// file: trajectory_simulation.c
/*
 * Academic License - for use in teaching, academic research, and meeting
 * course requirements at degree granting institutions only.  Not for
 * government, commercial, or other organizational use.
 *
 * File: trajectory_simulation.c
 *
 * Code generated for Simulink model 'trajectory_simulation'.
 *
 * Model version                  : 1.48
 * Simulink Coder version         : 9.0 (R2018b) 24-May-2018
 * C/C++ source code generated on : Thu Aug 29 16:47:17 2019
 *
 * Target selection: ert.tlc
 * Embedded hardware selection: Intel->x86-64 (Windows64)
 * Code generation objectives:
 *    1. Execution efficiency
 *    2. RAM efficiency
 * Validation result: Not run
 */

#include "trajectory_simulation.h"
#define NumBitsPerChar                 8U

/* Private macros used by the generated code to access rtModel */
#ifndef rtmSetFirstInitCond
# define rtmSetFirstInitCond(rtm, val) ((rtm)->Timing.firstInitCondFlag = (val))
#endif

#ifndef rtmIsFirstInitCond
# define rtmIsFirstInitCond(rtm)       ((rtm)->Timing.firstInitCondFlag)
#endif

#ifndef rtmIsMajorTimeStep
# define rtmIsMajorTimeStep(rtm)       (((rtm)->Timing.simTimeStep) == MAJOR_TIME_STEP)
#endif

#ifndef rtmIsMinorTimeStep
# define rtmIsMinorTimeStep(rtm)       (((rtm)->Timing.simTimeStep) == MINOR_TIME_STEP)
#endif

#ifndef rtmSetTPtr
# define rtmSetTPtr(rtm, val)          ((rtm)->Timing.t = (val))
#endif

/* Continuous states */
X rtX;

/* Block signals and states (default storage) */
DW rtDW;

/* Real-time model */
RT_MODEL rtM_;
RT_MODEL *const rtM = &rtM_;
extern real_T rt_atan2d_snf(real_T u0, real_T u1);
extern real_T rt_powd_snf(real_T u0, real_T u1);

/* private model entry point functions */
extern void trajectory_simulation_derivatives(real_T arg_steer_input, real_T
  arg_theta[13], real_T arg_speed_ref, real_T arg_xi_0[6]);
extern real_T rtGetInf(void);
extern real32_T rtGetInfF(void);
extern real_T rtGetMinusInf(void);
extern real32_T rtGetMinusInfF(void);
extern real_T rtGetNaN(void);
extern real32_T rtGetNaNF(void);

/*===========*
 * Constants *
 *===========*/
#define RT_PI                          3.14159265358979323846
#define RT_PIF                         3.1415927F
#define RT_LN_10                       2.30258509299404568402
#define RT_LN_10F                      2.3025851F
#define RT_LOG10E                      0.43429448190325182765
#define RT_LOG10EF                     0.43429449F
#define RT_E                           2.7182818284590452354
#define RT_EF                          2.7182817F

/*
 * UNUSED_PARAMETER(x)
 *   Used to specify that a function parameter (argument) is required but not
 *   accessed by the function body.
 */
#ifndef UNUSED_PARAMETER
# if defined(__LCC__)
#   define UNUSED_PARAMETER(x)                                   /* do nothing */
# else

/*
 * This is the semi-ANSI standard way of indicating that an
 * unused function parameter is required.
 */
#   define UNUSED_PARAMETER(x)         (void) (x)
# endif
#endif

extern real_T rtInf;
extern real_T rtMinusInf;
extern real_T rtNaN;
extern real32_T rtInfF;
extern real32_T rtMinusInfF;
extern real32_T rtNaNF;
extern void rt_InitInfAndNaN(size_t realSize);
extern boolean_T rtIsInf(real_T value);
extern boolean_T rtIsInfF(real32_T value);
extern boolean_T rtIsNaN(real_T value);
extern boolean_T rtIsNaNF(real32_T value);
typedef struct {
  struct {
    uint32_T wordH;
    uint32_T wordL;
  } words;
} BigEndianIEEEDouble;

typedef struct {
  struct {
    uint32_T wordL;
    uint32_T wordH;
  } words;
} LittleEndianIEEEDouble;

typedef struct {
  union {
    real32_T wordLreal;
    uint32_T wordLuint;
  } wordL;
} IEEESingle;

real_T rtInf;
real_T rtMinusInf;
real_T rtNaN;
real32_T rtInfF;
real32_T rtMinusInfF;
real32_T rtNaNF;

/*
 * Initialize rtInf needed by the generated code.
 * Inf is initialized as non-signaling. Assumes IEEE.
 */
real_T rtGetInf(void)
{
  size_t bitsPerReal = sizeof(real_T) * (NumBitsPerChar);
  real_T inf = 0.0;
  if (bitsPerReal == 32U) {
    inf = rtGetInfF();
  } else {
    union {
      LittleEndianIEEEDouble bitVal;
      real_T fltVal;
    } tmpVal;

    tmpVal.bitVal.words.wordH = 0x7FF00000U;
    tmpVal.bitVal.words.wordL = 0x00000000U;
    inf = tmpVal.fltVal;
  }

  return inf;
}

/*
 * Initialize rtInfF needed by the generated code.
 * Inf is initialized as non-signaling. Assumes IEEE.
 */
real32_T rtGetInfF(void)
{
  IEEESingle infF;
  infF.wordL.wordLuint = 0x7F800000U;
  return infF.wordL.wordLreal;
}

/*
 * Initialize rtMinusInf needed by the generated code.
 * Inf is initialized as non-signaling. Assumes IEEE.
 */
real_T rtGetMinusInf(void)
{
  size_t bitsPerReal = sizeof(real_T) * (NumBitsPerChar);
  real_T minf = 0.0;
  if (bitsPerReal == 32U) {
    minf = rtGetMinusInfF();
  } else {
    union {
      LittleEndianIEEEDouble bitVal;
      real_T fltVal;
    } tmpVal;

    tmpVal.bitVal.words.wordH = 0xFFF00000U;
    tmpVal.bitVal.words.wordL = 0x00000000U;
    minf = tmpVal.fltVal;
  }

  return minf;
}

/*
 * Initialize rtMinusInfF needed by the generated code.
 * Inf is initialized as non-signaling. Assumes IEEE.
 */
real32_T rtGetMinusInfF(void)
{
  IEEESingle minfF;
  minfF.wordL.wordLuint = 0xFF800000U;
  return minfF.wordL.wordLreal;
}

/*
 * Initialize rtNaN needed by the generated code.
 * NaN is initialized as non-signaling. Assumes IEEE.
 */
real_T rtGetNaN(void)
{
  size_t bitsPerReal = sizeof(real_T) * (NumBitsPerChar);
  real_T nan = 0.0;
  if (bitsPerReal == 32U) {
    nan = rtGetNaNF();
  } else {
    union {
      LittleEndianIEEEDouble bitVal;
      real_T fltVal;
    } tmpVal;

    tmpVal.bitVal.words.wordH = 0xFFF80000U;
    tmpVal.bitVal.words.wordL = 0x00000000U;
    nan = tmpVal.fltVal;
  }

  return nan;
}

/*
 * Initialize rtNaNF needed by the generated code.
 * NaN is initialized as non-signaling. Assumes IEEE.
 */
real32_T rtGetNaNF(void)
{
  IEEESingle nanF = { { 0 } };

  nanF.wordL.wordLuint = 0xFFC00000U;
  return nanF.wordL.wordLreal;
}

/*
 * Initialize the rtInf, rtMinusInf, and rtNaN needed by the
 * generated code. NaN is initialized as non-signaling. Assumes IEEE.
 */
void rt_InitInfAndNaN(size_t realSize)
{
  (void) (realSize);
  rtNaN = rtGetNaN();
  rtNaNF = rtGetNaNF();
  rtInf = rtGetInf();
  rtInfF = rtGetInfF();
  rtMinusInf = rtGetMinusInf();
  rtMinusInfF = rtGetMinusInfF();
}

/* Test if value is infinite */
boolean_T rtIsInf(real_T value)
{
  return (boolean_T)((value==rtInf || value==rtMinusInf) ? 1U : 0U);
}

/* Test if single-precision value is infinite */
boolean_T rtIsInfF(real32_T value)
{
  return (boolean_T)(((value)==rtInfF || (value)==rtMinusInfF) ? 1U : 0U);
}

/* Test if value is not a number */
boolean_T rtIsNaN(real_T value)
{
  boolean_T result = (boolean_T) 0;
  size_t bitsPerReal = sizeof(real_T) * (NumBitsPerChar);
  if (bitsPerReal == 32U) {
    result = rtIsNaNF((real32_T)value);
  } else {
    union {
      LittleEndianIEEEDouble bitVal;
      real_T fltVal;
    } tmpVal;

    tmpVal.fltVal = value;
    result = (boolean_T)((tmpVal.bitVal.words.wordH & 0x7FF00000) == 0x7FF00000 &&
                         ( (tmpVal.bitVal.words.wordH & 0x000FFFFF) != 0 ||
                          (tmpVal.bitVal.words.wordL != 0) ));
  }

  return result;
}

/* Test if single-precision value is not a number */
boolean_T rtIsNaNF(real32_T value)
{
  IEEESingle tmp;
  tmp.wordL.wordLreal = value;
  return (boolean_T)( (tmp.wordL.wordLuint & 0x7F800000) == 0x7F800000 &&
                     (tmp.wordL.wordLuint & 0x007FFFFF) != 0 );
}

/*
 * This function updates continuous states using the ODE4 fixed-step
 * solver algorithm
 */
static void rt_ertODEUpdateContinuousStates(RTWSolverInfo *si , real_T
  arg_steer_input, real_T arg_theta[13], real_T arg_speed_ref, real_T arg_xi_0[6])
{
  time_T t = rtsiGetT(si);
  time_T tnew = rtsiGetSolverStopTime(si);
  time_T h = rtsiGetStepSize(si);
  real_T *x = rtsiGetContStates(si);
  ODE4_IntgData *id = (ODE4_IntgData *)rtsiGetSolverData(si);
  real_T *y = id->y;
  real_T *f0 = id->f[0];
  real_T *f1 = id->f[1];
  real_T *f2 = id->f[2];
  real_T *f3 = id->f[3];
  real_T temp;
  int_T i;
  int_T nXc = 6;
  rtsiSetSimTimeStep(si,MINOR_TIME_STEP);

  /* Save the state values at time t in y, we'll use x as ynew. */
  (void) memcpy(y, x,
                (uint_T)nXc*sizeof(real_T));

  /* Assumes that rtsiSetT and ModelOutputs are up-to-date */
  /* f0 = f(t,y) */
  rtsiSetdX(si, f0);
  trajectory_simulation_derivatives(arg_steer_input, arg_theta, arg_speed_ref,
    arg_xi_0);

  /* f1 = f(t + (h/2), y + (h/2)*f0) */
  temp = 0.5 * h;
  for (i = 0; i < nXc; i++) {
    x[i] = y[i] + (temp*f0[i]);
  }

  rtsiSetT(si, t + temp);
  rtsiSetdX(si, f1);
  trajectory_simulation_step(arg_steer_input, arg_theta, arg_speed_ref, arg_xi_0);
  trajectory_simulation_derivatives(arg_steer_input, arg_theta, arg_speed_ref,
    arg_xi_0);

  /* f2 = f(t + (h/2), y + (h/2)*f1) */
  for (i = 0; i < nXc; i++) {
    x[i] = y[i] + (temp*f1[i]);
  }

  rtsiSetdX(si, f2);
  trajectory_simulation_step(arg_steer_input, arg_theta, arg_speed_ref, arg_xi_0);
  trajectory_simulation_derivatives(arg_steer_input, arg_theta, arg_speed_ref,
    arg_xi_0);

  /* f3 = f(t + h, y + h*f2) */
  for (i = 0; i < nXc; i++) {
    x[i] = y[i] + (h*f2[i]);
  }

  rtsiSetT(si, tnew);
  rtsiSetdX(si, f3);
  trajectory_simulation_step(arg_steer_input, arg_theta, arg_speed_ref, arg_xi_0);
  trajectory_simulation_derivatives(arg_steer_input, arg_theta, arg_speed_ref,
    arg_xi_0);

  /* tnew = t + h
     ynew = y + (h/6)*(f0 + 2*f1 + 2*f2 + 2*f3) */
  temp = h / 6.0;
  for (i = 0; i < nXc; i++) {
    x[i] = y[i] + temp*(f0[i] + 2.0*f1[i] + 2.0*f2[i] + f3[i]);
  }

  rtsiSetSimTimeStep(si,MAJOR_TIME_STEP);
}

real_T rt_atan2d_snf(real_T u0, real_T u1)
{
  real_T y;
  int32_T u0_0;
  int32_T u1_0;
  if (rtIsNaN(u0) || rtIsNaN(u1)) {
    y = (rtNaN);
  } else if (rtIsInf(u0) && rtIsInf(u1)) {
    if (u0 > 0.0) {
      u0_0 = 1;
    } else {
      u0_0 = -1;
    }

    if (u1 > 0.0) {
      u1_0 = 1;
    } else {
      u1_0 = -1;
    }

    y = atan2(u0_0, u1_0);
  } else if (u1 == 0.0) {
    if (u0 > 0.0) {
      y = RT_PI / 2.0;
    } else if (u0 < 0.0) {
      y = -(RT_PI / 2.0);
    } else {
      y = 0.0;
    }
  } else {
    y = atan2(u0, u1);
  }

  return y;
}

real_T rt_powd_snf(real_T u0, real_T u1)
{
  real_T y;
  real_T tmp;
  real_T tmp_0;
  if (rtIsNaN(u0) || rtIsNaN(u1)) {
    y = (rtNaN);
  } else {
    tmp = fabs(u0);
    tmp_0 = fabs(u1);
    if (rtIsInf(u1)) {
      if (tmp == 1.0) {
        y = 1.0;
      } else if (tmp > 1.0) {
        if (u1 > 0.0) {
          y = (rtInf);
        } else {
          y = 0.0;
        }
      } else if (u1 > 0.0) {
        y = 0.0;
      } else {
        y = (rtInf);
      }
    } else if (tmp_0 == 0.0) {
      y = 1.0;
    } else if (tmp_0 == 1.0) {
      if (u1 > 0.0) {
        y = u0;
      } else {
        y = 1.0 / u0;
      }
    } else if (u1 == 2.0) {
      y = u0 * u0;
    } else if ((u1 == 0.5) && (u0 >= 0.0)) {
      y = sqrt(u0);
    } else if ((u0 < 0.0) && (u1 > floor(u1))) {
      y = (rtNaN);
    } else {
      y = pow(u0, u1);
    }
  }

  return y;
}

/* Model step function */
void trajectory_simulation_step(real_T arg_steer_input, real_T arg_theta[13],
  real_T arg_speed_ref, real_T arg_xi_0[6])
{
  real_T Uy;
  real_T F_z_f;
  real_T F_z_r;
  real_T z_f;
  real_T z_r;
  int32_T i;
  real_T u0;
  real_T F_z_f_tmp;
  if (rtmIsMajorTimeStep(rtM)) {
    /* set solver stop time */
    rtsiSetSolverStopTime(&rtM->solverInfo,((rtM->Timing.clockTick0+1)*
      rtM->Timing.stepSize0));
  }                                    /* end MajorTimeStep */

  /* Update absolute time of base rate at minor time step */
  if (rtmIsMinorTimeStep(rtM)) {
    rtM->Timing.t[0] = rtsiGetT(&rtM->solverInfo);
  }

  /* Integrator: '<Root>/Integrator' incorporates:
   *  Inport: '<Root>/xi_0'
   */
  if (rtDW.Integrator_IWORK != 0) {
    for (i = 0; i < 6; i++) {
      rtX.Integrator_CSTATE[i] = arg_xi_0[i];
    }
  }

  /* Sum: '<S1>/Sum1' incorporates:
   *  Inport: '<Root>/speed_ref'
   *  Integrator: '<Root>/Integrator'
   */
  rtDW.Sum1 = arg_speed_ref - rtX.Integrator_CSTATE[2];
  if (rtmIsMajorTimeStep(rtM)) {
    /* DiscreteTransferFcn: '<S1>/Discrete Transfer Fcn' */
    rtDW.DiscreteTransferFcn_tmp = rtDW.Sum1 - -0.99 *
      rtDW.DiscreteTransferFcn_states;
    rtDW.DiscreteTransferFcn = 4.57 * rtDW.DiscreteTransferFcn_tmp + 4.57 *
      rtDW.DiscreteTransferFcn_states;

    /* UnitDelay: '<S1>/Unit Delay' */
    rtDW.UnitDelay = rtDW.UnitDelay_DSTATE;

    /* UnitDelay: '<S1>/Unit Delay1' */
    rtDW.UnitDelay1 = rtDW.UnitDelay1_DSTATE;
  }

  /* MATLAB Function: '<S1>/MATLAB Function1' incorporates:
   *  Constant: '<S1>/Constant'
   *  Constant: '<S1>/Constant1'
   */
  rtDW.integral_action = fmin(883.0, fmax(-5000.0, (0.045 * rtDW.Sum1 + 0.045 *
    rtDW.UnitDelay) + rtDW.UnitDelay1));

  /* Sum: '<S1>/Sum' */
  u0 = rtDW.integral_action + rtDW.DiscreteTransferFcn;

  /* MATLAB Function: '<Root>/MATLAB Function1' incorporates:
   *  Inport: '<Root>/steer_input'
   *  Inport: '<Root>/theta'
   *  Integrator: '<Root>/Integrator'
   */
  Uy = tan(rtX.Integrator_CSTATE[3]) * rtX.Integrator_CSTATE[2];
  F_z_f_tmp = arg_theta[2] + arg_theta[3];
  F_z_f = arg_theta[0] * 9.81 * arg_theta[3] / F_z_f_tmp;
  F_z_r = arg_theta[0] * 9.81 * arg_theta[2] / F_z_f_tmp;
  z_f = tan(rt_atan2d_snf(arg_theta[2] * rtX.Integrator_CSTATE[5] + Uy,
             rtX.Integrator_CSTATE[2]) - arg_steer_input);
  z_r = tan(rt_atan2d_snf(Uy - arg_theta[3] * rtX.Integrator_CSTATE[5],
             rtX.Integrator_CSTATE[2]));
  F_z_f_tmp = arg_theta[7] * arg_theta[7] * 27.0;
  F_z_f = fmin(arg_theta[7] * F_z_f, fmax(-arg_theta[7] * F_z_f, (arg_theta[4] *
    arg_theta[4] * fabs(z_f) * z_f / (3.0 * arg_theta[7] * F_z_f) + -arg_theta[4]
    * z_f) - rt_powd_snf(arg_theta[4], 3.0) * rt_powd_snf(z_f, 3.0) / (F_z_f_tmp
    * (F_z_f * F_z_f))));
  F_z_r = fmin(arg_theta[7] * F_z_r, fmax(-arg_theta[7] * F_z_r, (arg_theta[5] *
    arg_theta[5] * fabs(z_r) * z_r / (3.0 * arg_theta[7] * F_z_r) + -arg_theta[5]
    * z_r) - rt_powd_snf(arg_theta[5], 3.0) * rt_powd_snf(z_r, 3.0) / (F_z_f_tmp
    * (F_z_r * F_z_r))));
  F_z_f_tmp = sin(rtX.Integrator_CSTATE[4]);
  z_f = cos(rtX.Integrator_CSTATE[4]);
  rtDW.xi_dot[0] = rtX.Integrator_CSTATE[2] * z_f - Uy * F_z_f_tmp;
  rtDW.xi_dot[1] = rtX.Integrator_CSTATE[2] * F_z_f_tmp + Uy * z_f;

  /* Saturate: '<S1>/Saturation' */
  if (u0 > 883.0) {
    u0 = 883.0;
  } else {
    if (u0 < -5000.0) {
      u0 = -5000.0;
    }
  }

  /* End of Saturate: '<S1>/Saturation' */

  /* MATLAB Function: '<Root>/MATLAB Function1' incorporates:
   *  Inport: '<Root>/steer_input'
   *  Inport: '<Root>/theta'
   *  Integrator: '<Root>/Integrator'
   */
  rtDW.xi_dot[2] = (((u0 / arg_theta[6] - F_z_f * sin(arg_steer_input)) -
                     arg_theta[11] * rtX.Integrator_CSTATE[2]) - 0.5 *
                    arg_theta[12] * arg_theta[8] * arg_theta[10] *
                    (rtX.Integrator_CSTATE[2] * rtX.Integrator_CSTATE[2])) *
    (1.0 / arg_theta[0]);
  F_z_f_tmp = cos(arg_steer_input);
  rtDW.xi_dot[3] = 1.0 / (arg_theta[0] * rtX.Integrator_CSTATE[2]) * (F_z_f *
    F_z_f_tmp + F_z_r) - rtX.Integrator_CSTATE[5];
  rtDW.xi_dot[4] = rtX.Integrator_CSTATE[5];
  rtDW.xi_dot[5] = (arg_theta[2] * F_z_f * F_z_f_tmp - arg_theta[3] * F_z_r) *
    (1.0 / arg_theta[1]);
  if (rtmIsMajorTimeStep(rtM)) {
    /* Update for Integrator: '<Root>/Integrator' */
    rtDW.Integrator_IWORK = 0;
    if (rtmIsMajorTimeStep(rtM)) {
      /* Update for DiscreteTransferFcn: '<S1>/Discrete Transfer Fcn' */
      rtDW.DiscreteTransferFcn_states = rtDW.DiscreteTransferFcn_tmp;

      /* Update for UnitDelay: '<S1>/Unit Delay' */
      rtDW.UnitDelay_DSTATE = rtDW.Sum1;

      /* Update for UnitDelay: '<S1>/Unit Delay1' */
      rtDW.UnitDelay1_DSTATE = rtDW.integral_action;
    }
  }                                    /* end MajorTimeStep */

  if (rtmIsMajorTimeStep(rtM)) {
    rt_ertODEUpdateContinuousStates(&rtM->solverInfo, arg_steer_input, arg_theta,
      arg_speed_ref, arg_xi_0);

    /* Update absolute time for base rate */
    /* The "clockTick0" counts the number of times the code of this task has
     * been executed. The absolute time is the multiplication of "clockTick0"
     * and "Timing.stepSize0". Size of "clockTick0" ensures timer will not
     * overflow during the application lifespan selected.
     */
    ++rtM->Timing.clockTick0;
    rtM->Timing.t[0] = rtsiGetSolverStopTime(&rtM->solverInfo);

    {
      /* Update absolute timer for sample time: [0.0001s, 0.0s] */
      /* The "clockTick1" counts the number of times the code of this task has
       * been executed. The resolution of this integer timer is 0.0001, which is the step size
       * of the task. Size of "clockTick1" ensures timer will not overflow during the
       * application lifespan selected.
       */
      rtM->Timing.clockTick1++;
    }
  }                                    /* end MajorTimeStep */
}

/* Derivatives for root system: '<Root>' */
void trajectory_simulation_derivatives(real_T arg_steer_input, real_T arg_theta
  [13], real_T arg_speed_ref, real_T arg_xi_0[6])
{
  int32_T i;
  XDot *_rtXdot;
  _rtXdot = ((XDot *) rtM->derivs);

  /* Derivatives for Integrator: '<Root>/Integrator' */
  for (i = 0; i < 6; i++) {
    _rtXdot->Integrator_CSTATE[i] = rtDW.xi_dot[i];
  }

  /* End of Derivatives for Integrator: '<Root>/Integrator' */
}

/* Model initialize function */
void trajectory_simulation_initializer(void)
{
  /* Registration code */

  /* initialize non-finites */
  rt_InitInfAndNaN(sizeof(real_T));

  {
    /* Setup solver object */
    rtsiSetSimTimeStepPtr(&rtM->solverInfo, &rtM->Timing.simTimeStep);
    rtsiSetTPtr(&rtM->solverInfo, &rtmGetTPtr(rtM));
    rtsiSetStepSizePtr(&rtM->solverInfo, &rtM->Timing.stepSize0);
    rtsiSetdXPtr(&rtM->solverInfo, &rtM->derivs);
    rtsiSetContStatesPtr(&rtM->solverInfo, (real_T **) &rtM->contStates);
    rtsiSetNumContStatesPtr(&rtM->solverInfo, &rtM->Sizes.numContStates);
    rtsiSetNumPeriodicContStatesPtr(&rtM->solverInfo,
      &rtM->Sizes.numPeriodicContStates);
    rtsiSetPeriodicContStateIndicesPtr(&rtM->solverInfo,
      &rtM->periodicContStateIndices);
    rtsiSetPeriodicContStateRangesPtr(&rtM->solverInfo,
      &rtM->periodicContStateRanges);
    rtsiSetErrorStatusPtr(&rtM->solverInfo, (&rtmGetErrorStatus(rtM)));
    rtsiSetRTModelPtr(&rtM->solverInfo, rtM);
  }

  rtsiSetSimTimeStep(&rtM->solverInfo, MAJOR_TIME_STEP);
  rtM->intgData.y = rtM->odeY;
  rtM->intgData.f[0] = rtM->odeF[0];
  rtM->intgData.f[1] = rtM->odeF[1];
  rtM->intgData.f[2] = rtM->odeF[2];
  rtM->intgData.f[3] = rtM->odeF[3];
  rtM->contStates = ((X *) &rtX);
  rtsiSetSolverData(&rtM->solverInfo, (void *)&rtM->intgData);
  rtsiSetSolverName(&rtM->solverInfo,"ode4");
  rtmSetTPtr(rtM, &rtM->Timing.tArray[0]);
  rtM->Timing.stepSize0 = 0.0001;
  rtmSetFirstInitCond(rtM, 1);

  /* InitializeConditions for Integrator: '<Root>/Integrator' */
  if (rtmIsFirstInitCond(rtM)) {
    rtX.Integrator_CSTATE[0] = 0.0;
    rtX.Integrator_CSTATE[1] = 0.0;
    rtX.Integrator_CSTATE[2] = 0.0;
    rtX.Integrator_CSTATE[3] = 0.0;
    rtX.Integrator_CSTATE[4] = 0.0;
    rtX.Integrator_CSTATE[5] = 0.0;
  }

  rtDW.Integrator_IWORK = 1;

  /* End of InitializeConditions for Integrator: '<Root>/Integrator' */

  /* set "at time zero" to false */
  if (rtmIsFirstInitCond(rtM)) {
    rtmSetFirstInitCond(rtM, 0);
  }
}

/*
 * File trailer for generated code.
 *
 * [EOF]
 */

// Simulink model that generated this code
simulink model "trajectory_simulation"  (R2018b)
settings: Solver=ode4  StartTime=0.0  StopTime=25  FixedStep=1e-4  RelTol=1e-3
undefined symbols (not defined in the file or in its folder): xi_0

== system trajectory_simulation ==
  steer_input : Inport  OutDataTypeStr=double  PortDimensions=1
  theta : Inport  Port=2  OutDataTypeStr=double  PortDimensions=13
  speed_ref : Inport  Port=3  OutDataTypeStr=double  PortDimensions=1
  xi_0 : Inport  Port=4  OutDataTypeStr=double  PortDimensions=6
  Cruise Control : Subsystem
  Demux : Demux  Outputs=6
  Integrator : Integrator  InitialConditionSource=external  InitialCondition=xi_0
  MATLAB Function1 : MATLAB Function  TreatAsAtomicUnit=on
  Mux : Mux  Inputs=2
  Mux1 : Mux  Inputs=2
  Terminator3 : Terminator
  Terminator4 : Terminator
  Terminator5 : Terminator
  To Workspace : ToWorkspace  VariableName=traj  SaveFormat=Structure With Time  SampleTime=-1
  wires:
  steer_input/1 -> Mux/2
  Cruise Control/1(Out1) -> [Torque]  "Torque"
  [Torque] -> Mux/1
  speed_ref/1 -> Cruise Control/1(In1)
  Demux/3 -> Cruise Control/2(In2)
  Demux/1 -> Mux1/1
  Demux/2 -> Mux1/2
  Demux/4 -> Terminator3/1
  Demux/5 -> Terminator4/1
  Demux/6 -> Terminator5/1
  Integrator/1 -> Demux/1, MATLAB Function1/1(xi_internal)
  MATLAB Function1/1(xi_dot) -> Integrator/1
  theta/1 -> MATLAB Function1/3(theta_internal)
  Mux/1 -> MATLAB Function1/2(u_internal)
  xi_0/1 -> Integrator/2
  Mux1/1 -> To Workspace/1

== system trajectory_simulation/Cruise Control ==
  In1 : Inport
  In2 : Inport  Port=2
  "  " : Constant  Value=[0.045,0.045]
  Constant : Constant  Value=883
  Constant1 : Constant  Value=-5000
  Discrete Transfer Fcn : DiscreteTransferFcn  Numerator=[ 4.57,4.57 ]  Denominator=[ 1,-0.99 ]
  MATLAB Function1 : MATLAB Function  TreatAsAtomicUnit=on
  Saturation : Saturate  UpperLimit=883  LowerLimit=-5000
  Sum : Sum
  Sum1 : Sum  Inputs=+-
  Unit Delay : UnitDelay  SampleTime=-1
  Unit Delay1 : UnitDelay  SampleTime=-1
  Out1 : Outport
  wires:
  Constant1/1 -> MATLAB Function1/5(Td_min)
  Unit Delay/1 -> MATLAB Function1/2(err_m1)
  [Ref_err] -> Unit Delay/1, MATLAB Function1/1(err)
  Constant/1 -> MATLAB Function1/4(Td_max)
  MATLAB Function1/1(integral_action) -> Sum/1, Unit Delay1/1
  Discrete Transfer Fcn/1 -> Sum/2
  Sum/1 -> Saturation/1
  In1/1 -> Sum1/1
  In2/1 -> Sum1/2
  Sum1/1 -> [Ref_err]
  [Ref_err] -> Discrete Transfer Fcn/1
  Saturation/1 -> Out1/1
  "  "/1 -> MATLAB Function1/6(num_int)
  Unit Delay1/1 -> MATLAB Function1/3(integral_m1)

== matlab function trajectory_simulation/Cruise Control/MATLAB Function1 ==
function integral_action = integrator_anti_wu(err, err_m1, integral_m1, Td_max, Td_min, num_int)

integral_action = min(Td_max, max(Td_min, integral_m1+num_int'*[err;err_m1]));

== matlab function trajectory_simulation/MATLAB Function1 ==
function xi_dot = vehicle(xi_internal, u_internal, theta_internal)
% simulation, time has to be the fist input

%% Read states
X = xi_internal(1,1);
Y = xi_internal(2,1);
Ux = xi_internal(3,1);
beta = xi_internal(4,1);
psi = xi_internal(5,1);
r = xi_internal(6,1);

%% Read Inputs

Td_internal = u_internal(1,1);
delta_internal = u_internal(2,1);

%% Read Parameters

m = theta_internal(1,1);
Jz = theta_internal(2,1);
a = theta_internal(3,1);
b = theta_internal(4,1);
Cf = theta_internal(5,1);
Cr = theta_internal(6,1);
rw = theta_internal(7,1);
mu = theta_internal(8,1);
Af = theta_internal(9,1);
Al = theta_internal(10,1);
Cx = theta_internal(11,1);
Rr = theta_internal(12,1);
rho = theta_internal(13,1);
g = 9.81;

%% Equations

Uy = tan(beta)*Ux;
alfa_f = atan2((Uy + a*r),Ux) - delta_internal;
alfa_r = atan2((Uy - b*r),Ux);

F_z_f = m * g * b / (a+b);
F_z_r = m * g * a / (a+b);

z_f = tan(alfa_f);
z_r = tan(alfa_r);

elem1 = mu*F_z_f;
elem21 = - mu*F_z_f;
elem22 = - Cf*z_f + (Cf^2*abs(z_f)*z_f)/(3*mu*F_z_f) - (Cf^3*z_f^3)/(27*mu^2*F_z_f^2);
elem2 = max(elem21,elem22);
F_y_f = min(elem1, elem2);

elem1 = mu*F_z_r;
elem21 = - mu*F_z_r;
elem22 = - Cr*z_r + (Cr^2*abs(z_r)*z_r)/(3*mu*F_z_r) - (Cr^3*z_r^3)/(27*mu^2*F_z_r^2);
elem2 = max(elem21,elem22);
F_y_r = min(elem1,elem2);

F_x = Td_internal/rw;

F_r = Rr*Ux;
F_x_d = 0.5*rho*Af*Cx*Ux^2;

%% Output
xi_dot = zeros(6,1);
xi_dot(1,1) = Ux*cos(psi) - Uy*sin(psi);
xi_dot(2,1) = Ux*sin(psi)+ Uy*cos(psi);
xi_dot(3,1) = 1/m * ((F_x - F_y_f*sin(delta_internal))-F_r-F_x_d);
xi_dot(4,1) = 1/(m*Ux) * (F_y_f*cos(delta_internal)+F_y_r) - r;
xi_dot(5,1) = r;
xi_dot(6,1) = 1/Jz * (a*F_y_f*cos(delta_internal) - b* F_y_r);
% Forces = zeros(3,1);
% Forces(1,1) = F_y_f;
% Forces(2,1) = F_y_r;
% Forces(3,1) = F_x;

end
